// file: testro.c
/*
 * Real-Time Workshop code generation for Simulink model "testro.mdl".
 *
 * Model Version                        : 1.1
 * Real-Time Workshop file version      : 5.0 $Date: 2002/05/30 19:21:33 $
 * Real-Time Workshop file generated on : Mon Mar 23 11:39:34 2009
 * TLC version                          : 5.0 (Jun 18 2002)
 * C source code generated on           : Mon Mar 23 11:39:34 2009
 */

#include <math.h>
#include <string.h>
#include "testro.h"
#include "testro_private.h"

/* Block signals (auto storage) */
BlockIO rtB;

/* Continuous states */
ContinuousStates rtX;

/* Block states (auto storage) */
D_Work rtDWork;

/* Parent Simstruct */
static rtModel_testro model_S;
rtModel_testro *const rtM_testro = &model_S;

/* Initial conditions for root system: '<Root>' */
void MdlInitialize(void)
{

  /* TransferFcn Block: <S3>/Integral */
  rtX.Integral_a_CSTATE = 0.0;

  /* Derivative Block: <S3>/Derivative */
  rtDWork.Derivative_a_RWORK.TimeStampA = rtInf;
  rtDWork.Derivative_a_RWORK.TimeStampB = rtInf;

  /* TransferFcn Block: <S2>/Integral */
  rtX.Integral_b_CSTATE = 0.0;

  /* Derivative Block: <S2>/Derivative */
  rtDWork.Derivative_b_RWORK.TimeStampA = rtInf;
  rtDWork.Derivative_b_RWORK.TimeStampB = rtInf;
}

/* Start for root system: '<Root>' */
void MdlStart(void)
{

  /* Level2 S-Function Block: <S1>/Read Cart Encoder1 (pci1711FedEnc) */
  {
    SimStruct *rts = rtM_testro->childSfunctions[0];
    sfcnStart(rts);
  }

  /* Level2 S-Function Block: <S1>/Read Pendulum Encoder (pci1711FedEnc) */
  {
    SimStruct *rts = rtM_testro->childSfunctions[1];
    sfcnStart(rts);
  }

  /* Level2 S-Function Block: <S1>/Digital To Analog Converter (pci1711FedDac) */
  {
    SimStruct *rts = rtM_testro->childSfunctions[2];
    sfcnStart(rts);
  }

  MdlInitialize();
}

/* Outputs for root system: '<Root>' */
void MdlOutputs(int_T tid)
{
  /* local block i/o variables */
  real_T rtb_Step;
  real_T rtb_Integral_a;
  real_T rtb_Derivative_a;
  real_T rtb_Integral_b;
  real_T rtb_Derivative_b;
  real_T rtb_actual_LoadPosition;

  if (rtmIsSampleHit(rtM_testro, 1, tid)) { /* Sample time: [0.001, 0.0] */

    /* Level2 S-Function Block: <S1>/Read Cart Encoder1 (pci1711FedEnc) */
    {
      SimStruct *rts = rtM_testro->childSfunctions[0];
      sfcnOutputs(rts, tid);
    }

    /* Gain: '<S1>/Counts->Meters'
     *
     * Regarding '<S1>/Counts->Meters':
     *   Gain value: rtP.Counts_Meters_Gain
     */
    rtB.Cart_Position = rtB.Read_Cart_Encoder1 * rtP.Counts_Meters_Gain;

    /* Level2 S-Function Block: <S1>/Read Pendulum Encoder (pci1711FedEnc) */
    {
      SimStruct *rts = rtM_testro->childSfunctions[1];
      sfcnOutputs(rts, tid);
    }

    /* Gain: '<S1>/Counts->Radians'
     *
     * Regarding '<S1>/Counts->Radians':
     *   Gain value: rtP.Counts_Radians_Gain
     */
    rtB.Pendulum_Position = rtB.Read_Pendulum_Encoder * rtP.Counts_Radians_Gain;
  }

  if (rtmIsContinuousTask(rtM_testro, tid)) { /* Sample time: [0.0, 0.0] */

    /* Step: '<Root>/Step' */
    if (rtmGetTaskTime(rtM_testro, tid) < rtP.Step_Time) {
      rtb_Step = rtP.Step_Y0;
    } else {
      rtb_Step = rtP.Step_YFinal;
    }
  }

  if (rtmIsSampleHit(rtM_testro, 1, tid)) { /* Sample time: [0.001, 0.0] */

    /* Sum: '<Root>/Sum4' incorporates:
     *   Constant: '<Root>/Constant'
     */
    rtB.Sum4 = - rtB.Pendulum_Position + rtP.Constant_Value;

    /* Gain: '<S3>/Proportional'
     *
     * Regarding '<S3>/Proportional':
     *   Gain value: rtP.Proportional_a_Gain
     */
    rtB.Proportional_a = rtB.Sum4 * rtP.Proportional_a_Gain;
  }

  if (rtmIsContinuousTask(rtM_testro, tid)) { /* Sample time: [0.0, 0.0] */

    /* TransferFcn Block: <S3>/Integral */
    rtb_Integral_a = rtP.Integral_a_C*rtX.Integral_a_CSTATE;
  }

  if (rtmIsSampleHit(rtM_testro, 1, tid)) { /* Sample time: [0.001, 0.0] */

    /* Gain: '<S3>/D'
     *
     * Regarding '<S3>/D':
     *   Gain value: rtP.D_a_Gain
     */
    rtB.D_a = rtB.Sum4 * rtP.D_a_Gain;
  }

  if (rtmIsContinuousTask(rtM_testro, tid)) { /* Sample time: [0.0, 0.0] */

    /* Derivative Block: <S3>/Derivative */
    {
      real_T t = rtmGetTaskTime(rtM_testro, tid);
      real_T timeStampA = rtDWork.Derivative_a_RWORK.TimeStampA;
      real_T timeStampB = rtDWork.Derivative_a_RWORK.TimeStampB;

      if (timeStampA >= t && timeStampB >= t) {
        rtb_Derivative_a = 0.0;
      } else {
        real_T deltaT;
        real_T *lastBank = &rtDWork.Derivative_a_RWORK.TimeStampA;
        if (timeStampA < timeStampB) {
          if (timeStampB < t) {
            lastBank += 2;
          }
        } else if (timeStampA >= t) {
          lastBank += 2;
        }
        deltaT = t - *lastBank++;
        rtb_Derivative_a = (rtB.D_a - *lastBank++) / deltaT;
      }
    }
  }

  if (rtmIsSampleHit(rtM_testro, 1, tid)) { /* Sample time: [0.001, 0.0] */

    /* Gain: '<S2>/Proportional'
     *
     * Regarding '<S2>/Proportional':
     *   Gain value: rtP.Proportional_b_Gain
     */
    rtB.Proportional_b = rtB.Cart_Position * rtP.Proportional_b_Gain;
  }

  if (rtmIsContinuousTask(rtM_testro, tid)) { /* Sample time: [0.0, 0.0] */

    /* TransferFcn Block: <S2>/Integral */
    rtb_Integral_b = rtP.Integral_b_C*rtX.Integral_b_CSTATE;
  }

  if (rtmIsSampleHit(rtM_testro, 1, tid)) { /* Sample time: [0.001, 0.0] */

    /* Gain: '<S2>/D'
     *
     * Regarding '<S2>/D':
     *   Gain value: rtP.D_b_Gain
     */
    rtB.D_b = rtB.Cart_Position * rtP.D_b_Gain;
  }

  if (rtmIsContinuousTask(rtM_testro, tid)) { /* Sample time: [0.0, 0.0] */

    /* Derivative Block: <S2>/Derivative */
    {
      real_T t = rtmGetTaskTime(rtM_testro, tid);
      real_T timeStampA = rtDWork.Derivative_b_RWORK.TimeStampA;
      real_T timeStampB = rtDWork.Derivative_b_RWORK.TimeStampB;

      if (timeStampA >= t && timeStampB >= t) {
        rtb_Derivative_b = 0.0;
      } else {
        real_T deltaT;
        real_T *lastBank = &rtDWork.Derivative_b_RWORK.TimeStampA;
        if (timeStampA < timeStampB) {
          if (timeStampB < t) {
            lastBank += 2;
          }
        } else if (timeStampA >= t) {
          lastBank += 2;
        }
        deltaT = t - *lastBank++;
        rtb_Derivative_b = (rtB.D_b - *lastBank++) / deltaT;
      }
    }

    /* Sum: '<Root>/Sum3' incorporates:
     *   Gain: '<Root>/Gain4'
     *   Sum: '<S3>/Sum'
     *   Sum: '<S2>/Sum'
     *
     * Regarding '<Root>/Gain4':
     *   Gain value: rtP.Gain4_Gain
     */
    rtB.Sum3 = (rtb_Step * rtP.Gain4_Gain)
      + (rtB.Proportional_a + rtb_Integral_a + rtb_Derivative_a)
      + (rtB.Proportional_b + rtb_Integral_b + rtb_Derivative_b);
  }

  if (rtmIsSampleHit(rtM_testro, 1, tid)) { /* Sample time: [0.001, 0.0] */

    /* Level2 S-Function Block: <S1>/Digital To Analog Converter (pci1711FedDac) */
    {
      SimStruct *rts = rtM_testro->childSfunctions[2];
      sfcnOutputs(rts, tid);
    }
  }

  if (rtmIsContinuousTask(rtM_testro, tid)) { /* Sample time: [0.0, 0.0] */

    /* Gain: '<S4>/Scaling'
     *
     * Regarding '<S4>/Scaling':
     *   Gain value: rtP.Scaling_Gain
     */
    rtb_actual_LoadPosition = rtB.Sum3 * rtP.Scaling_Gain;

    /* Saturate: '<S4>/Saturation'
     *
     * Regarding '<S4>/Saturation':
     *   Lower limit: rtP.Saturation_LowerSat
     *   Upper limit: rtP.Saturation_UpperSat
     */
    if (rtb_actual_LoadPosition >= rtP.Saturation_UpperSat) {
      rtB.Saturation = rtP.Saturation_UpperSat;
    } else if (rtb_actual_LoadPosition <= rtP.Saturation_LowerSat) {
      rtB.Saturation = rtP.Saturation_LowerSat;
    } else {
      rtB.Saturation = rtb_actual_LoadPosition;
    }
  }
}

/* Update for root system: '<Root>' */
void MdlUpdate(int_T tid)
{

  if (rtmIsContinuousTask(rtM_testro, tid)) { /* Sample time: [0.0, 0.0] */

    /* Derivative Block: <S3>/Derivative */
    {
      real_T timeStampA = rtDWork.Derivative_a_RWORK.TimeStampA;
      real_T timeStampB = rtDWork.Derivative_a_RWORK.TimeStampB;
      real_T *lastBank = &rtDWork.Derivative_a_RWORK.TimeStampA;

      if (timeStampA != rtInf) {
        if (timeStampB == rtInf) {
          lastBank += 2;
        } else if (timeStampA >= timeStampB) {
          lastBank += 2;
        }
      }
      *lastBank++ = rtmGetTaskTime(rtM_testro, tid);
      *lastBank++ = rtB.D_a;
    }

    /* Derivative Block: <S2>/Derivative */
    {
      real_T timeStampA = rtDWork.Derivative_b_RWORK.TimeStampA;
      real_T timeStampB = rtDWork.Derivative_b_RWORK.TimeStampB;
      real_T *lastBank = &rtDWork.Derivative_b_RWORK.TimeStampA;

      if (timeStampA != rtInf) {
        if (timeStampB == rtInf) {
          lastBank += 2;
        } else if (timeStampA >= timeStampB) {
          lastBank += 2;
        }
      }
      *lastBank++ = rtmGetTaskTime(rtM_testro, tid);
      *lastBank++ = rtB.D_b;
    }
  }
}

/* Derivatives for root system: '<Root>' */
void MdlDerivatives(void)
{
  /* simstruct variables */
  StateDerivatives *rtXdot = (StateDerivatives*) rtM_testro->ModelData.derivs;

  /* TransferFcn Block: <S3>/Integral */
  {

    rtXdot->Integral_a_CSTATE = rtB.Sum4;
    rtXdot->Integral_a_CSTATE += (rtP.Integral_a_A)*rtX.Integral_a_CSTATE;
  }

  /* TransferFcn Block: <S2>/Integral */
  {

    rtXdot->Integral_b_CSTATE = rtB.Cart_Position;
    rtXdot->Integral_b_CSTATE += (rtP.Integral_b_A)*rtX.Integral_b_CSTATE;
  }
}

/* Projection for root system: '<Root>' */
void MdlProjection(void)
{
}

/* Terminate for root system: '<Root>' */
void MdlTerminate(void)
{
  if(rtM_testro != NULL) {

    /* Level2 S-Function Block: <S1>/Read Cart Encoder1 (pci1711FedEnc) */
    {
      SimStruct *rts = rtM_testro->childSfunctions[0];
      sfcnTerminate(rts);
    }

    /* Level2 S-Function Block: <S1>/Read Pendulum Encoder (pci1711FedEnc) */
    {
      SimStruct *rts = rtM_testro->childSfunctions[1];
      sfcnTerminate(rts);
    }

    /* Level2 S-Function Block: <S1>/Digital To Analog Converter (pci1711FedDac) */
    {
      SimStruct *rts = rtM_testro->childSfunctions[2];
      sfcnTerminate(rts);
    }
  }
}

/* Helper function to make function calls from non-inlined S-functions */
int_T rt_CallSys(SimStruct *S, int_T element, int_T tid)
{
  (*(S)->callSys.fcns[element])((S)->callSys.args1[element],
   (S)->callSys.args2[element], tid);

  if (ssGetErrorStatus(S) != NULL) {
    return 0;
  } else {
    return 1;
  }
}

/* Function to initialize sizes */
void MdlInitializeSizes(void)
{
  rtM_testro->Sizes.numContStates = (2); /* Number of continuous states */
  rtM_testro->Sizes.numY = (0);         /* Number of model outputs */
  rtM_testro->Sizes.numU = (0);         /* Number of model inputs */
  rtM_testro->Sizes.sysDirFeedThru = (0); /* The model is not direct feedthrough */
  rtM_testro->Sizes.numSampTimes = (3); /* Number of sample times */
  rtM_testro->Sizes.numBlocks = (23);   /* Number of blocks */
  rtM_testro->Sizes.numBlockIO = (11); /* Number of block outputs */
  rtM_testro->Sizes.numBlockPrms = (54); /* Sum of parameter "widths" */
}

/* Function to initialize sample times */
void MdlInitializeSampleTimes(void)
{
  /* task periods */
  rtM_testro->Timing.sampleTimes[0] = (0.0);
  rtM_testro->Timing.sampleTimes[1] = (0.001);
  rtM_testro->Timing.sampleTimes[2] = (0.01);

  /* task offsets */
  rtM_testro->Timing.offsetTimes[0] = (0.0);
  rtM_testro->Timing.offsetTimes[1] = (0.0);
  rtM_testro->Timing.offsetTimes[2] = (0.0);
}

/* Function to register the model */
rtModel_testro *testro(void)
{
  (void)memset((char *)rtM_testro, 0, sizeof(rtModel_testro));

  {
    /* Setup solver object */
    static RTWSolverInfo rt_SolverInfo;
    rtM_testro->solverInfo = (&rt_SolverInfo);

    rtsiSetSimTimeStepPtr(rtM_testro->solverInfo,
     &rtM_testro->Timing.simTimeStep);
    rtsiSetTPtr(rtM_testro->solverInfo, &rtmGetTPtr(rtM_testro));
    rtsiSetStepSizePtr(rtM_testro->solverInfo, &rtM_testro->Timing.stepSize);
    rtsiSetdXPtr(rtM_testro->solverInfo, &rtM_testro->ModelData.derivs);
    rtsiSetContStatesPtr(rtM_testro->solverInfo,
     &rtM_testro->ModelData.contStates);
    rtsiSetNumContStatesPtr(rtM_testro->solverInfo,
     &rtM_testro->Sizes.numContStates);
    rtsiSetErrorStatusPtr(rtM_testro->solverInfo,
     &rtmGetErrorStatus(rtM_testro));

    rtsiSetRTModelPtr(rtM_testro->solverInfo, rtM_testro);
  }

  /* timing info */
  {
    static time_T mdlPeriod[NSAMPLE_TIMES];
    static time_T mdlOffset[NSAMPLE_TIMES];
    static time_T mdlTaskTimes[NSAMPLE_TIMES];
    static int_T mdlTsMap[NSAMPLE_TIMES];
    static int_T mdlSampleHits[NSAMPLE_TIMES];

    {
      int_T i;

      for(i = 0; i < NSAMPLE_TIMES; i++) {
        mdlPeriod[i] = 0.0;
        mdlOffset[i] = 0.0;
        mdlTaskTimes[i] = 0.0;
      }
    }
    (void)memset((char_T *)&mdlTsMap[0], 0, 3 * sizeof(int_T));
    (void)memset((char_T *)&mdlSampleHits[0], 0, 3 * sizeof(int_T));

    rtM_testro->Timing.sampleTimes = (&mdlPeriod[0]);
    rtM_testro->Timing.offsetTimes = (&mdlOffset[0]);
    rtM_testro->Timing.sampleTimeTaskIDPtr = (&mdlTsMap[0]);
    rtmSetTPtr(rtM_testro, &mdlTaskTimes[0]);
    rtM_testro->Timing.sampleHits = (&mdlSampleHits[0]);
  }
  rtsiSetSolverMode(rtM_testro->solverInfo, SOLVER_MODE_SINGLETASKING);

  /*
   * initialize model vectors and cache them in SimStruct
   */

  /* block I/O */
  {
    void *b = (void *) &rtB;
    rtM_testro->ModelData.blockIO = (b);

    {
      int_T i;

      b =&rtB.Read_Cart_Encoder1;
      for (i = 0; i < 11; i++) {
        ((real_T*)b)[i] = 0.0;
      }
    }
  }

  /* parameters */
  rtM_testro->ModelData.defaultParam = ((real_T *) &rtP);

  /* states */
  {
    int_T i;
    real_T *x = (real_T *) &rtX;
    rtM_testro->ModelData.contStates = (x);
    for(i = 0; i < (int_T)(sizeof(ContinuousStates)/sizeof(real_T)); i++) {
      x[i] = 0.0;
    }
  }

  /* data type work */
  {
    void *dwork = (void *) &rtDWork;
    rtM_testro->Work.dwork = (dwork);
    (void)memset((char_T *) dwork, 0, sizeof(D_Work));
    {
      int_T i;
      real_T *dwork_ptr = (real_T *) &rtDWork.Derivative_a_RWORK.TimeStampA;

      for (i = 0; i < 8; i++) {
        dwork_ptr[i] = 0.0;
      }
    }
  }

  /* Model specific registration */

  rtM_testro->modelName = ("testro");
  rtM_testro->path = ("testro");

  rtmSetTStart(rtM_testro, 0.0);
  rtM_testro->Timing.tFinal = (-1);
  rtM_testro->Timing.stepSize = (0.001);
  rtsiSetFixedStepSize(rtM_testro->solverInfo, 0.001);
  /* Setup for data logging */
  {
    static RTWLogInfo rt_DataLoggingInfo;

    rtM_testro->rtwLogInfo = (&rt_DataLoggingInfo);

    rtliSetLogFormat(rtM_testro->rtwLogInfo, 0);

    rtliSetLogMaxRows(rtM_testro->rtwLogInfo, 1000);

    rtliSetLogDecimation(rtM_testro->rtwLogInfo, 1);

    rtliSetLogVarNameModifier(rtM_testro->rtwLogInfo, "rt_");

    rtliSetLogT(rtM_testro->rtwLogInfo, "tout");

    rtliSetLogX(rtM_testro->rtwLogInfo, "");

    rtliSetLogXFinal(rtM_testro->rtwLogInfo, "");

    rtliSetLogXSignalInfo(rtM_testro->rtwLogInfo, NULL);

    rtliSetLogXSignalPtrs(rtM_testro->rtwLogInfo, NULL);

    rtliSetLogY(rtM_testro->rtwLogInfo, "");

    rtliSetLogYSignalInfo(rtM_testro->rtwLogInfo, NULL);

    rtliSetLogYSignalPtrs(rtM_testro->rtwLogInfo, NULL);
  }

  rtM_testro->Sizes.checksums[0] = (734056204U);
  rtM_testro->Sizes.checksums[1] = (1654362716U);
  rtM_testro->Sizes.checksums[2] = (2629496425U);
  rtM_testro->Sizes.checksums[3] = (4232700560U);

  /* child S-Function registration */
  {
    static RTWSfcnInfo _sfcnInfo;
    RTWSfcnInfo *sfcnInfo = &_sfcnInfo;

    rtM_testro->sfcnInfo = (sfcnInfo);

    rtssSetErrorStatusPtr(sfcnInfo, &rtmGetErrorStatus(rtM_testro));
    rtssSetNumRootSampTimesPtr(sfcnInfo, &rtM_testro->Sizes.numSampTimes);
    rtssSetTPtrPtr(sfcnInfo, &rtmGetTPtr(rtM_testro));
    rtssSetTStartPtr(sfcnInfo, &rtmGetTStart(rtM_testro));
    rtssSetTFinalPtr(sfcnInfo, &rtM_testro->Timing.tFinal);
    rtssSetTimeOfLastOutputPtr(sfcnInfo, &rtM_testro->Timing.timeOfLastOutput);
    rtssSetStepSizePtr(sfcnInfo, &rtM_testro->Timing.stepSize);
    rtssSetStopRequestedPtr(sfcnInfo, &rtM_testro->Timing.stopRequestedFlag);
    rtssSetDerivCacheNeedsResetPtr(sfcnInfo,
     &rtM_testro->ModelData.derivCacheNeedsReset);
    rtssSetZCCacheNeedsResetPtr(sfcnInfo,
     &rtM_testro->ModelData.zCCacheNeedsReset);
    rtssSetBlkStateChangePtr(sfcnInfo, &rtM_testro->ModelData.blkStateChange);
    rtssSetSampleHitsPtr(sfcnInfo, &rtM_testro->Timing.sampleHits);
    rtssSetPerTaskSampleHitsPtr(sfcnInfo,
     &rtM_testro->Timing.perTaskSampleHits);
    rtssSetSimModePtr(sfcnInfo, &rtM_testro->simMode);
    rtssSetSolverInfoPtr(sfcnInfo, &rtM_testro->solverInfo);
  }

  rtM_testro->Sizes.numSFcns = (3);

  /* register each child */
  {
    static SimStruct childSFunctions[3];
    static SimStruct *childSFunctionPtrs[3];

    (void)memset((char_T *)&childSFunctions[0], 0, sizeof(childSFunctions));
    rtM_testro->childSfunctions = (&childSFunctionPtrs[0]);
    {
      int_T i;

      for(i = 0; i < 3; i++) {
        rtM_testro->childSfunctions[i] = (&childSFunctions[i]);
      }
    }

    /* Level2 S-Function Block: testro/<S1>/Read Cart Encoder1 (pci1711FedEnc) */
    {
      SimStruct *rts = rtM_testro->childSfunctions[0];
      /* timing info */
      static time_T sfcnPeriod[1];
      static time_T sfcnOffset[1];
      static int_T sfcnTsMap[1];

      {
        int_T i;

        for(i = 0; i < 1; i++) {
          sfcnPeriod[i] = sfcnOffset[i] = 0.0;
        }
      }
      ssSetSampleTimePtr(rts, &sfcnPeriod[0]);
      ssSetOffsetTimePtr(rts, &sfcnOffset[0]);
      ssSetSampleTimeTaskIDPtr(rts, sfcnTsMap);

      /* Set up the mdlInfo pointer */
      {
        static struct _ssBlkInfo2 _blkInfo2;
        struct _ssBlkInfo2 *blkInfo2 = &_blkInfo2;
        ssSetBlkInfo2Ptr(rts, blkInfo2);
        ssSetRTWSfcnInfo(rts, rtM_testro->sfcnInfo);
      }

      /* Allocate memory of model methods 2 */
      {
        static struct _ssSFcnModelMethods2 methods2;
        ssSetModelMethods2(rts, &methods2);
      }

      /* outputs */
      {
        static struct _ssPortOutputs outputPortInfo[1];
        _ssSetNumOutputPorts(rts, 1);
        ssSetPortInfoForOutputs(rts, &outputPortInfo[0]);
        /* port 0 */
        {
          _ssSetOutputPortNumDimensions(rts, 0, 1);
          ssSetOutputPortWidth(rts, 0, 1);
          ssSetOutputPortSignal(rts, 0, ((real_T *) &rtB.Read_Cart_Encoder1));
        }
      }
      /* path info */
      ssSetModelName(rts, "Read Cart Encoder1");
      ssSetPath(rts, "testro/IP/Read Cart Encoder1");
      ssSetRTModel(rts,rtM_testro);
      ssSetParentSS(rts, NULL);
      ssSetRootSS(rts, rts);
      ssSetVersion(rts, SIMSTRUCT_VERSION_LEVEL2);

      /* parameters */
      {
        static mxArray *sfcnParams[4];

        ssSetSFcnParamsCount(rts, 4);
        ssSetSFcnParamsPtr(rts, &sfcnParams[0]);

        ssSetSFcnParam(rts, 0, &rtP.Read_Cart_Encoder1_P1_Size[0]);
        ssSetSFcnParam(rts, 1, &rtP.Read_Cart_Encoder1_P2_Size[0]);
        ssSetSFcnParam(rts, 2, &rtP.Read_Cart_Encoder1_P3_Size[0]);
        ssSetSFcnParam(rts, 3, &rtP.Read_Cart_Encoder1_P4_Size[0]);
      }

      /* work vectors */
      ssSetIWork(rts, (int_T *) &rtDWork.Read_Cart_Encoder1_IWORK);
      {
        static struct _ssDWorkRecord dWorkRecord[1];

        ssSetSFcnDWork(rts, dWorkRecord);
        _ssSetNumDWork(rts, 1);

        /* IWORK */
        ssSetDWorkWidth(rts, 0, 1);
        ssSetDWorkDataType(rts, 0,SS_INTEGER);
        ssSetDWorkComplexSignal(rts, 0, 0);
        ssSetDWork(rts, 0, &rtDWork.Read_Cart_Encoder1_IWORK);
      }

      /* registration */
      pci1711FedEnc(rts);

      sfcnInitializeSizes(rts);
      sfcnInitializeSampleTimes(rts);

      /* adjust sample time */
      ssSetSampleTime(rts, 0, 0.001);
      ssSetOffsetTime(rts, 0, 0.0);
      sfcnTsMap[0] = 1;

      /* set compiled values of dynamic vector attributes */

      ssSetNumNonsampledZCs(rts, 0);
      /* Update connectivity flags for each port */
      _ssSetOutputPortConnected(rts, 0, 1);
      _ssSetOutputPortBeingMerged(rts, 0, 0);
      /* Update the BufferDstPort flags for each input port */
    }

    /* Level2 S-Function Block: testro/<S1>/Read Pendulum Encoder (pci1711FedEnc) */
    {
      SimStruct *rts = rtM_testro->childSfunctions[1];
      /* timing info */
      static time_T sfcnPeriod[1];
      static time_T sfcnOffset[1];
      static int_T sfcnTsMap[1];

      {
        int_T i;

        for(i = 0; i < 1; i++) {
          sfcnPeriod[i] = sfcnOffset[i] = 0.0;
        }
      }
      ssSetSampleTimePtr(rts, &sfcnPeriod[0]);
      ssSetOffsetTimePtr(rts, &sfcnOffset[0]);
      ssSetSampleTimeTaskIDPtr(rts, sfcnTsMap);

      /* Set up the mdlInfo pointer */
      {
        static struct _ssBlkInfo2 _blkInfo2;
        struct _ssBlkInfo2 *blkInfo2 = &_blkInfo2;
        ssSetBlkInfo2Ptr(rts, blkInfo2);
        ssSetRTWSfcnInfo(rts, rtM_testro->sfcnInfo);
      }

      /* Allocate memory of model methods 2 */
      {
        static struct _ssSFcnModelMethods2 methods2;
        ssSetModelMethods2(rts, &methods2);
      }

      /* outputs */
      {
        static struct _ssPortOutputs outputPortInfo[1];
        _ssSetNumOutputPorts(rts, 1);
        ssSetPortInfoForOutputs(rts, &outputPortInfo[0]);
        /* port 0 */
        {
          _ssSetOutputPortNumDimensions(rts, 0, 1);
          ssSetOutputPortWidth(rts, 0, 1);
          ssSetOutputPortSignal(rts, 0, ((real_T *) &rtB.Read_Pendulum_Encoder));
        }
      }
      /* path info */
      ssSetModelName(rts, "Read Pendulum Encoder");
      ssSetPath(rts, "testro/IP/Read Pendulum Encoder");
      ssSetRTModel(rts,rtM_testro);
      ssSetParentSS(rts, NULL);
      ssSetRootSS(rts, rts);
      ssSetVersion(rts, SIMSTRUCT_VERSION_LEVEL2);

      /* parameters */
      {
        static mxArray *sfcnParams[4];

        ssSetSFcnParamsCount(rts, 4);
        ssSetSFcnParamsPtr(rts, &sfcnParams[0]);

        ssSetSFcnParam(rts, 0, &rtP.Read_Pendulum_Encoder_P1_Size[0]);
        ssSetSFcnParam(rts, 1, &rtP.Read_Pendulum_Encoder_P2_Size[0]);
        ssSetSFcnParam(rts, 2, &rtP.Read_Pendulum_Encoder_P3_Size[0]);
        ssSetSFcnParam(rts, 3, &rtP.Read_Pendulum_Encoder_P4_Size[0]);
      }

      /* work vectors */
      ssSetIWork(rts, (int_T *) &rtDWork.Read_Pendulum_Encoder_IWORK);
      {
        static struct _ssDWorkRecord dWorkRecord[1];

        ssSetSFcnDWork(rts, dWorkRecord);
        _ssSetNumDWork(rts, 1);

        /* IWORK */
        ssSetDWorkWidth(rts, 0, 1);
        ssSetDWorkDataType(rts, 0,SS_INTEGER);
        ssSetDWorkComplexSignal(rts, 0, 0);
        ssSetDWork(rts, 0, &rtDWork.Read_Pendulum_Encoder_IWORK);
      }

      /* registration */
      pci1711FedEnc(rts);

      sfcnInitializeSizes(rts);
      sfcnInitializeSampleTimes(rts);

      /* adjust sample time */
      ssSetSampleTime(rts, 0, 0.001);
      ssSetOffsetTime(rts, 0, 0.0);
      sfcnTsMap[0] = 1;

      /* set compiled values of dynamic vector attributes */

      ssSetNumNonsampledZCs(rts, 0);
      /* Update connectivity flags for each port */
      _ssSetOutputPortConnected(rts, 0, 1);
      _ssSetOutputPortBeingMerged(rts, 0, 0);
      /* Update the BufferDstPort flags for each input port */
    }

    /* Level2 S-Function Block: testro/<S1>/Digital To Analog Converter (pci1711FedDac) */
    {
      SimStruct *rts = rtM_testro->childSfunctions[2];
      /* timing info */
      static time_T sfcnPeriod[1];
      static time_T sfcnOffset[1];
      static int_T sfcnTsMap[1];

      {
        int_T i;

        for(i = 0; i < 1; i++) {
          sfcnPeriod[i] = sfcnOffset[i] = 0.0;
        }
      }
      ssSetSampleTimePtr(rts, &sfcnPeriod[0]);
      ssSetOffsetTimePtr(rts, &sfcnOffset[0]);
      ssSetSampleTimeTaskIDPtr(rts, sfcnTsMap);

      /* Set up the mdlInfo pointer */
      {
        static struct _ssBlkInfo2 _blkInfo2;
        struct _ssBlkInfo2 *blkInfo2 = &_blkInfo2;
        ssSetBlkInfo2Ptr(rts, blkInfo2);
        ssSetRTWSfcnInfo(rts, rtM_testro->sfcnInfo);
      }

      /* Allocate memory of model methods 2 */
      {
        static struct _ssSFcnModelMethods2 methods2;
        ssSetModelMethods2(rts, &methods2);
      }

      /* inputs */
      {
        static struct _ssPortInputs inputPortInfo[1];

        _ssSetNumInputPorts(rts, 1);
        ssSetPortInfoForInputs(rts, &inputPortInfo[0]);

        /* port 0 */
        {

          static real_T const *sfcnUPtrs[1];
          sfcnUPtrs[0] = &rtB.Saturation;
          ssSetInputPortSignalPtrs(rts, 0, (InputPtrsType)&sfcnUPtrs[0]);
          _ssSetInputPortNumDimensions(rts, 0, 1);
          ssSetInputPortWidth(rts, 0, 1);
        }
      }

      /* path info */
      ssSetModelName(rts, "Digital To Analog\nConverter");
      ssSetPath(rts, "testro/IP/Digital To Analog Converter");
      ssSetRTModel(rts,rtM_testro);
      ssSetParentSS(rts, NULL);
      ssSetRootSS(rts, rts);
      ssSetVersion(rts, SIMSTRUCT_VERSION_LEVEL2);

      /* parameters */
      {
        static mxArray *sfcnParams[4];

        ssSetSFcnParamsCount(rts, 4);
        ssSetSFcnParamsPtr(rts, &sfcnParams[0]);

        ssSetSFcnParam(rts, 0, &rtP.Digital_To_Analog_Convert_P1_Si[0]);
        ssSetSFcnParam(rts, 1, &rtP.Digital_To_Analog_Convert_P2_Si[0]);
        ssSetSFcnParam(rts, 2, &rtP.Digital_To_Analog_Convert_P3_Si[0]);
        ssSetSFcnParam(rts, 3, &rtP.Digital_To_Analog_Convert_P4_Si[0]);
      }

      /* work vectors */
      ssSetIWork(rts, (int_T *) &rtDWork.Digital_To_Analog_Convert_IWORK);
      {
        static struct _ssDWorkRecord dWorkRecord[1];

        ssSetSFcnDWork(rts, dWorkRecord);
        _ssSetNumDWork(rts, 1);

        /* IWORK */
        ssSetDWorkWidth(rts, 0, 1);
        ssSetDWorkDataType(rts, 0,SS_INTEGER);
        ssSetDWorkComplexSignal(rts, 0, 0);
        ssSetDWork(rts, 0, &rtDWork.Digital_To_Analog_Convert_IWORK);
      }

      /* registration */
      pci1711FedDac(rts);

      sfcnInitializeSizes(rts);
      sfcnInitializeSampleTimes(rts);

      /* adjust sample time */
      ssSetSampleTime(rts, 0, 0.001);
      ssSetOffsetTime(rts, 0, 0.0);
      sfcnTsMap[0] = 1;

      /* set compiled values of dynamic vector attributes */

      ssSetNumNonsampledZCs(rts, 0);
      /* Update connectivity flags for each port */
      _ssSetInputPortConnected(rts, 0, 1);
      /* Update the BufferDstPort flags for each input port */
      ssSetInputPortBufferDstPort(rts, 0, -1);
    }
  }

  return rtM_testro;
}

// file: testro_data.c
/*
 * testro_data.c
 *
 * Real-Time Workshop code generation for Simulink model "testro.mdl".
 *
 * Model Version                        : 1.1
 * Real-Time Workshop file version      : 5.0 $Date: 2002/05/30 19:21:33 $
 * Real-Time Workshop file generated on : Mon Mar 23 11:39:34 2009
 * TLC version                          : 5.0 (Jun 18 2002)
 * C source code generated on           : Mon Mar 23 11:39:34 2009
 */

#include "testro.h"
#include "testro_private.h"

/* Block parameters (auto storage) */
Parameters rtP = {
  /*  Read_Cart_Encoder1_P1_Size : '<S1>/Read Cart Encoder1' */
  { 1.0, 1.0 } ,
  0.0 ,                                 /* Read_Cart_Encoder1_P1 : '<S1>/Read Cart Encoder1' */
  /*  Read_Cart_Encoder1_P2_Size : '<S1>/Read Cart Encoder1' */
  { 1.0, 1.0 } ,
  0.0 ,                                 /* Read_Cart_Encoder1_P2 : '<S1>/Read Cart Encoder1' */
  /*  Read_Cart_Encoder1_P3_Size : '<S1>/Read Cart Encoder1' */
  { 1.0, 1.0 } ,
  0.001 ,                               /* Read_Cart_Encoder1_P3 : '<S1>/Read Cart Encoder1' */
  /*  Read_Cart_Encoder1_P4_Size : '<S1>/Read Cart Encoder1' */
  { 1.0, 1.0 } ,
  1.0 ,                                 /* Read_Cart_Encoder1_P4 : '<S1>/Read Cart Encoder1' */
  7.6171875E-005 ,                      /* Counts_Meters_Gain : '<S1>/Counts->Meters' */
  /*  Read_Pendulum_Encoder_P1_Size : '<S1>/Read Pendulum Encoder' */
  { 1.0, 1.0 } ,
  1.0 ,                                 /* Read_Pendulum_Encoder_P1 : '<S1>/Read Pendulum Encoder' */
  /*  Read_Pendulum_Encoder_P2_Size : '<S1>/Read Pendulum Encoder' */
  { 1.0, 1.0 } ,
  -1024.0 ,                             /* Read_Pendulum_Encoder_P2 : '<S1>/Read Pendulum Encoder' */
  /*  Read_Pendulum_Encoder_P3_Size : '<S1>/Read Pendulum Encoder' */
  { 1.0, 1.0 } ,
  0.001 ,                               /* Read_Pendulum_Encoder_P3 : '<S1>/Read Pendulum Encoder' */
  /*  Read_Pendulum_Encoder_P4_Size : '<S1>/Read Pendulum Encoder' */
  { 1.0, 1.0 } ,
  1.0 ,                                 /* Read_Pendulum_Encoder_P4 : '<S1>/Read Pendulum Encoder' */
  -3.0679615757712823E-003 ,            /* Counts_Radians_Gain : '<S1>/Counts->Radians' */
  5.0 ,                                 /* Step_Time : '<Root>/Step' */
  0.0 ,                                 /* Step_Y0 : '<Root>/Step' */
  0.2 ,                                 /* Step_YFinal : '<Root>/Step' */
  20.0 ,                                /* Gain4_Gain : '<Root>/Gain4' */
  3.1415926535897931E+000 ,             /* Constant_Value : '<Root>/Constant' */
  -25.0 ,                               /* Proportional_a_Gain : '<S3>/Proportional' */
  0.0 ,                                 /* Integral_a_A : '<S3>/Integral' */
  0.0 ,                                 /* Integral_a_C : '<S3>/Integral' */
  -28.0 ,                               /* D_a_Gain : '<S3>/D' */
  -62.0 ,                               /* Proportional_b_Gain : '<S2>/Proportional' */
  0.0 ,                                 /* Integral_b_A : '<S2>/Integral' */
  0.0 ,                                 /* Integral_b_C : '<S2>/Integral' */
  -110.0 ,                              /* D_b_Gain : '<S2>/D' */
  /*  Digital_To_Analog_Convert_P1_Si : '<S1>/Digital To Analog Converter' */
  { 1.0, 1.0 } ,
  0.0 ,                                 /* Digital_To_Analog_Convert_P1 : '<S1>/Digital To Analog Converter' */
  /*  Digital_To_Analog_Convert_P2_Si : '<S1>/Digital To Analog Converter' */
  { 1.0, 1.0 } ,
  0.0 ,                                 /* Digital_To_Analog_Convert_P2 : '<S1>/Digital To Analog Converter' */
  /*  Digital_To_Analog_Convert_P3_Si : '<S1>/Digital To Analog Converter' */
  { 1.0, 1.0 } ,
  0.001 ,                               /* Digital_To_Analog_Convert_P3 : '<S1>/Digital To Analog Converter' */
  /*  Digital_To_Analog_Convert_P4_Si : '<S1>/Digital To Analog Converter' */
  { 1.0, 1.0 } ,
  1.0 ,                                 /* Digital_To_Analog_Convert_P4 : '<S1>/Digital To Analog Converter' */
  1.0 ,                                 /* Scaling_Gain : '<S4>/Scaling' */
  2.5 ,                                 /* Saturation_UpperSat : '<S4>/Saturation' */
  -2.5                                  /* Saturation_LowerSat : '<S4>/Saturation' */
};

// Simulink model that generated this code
simulink model "testro"  (Simulink 5.0)
settings: Solver=ode45  StartTime=0.0  StopTime=10.0  RelTol=1e-3
libraries: pci1711 x3, simulink_extras x2

== system testro ==
  Constant : Constant  Value=pi
  Gain4 : Gain  Gain=20  SaturateOnIntegerOverflow=on
  IP : Subsystem
  PID Controller : simulink_extras/Additional Linear/PID Controller  Orientation=left  P=-31*2  I=0  D=-110
  PID Controller1 : simulink_extras/Additional Linear/PID Controller  Orientation=left  P=-25  I=0  D=-28
  Scope : Scope  NumInputPorts=3
  Step : Step  Time=5  After=0.2  SampleTime=0
  Sum3 : Sum  Inputs=|+++  SaturateOnIntegerOverflow=on
  Sum4 : Sum  Orientation=left  Inputs=|-+  SaturateOnIntegerOverflow=on
  wires:
  IP/1(position) -> PID Controller/1, Scope/1
  IP/2(angle) -> Sum4/1, Scope/2
  Sum3/1 -> Scope/3, IP/1(u)
  Gain4/1 -> Sum3/1
  Step/1 -> Gain4/1
  PID Controller/1 -> Sum3/3
  PID Controller1/1 -> Sum3/2
  Constant/1 -> Sum4/2
  Sum4/1 -> PID Controller1/1

== system testro/IP ==
  u : Inport
  Counts->Meters : Gain  Gain=.156/2048  SaturateOnIntegerOverflow=on
  Counts->Radians : Gain  Gain=-2*pi/2048  SaturateOnIntegerOverflow=on
  Digital To Analog Converter : pci1711/Advantech  PCI1711 I//O Board Lib/Feedback DAC  channel=0  range=0  tsamp=0.001  hwAccess=on
  Read Cart Encoder1 : pci1711/Advantech  PCI1711 I//O Board Lib/Feedback Encoder   channel=0  offset=0  tsamp=0.001  hwAccess=on
  Read Pendulum Encoder : pci1711/Advantech  PCI1711 I//O Board Lib/Feedback Encoder   channel=1  offset=-1024  tsamp=0.001  hwAccess=on
  Scaling and Safety : Subsystem
  position : Outport
  angle : Outport  Port=2
  wires:
  Scaling and Safety/1(Out1) -> Digital To Analog Converter/1
  u/1 -> Scaling and Safety/1(In1)
  Read Cart Encoder1/1 -> Counts->Meters/1
  Read Pendulum Encoder/1 -> Counts->Radians/1
  Counts->Radians/1 -> angle/1  "Pendulum Position"
  Counts->Meters/1 -> position/1  "Cart Position"

== system testro/IP/Scaling and Safety ==
  In1 : Inport
  Saturation : Saturate  UpperLimit=2.5  LowerLimit=-2.5
  Scaling : Gain  SaturateOnIntegerOverflow=on
  Out1 : Outport
  wires:
  Scaling/1 -> Saturation/1  "actual LoadPosition"
  In1/1 -> Scaling/1
  Saturation/1 -> Out1/1
